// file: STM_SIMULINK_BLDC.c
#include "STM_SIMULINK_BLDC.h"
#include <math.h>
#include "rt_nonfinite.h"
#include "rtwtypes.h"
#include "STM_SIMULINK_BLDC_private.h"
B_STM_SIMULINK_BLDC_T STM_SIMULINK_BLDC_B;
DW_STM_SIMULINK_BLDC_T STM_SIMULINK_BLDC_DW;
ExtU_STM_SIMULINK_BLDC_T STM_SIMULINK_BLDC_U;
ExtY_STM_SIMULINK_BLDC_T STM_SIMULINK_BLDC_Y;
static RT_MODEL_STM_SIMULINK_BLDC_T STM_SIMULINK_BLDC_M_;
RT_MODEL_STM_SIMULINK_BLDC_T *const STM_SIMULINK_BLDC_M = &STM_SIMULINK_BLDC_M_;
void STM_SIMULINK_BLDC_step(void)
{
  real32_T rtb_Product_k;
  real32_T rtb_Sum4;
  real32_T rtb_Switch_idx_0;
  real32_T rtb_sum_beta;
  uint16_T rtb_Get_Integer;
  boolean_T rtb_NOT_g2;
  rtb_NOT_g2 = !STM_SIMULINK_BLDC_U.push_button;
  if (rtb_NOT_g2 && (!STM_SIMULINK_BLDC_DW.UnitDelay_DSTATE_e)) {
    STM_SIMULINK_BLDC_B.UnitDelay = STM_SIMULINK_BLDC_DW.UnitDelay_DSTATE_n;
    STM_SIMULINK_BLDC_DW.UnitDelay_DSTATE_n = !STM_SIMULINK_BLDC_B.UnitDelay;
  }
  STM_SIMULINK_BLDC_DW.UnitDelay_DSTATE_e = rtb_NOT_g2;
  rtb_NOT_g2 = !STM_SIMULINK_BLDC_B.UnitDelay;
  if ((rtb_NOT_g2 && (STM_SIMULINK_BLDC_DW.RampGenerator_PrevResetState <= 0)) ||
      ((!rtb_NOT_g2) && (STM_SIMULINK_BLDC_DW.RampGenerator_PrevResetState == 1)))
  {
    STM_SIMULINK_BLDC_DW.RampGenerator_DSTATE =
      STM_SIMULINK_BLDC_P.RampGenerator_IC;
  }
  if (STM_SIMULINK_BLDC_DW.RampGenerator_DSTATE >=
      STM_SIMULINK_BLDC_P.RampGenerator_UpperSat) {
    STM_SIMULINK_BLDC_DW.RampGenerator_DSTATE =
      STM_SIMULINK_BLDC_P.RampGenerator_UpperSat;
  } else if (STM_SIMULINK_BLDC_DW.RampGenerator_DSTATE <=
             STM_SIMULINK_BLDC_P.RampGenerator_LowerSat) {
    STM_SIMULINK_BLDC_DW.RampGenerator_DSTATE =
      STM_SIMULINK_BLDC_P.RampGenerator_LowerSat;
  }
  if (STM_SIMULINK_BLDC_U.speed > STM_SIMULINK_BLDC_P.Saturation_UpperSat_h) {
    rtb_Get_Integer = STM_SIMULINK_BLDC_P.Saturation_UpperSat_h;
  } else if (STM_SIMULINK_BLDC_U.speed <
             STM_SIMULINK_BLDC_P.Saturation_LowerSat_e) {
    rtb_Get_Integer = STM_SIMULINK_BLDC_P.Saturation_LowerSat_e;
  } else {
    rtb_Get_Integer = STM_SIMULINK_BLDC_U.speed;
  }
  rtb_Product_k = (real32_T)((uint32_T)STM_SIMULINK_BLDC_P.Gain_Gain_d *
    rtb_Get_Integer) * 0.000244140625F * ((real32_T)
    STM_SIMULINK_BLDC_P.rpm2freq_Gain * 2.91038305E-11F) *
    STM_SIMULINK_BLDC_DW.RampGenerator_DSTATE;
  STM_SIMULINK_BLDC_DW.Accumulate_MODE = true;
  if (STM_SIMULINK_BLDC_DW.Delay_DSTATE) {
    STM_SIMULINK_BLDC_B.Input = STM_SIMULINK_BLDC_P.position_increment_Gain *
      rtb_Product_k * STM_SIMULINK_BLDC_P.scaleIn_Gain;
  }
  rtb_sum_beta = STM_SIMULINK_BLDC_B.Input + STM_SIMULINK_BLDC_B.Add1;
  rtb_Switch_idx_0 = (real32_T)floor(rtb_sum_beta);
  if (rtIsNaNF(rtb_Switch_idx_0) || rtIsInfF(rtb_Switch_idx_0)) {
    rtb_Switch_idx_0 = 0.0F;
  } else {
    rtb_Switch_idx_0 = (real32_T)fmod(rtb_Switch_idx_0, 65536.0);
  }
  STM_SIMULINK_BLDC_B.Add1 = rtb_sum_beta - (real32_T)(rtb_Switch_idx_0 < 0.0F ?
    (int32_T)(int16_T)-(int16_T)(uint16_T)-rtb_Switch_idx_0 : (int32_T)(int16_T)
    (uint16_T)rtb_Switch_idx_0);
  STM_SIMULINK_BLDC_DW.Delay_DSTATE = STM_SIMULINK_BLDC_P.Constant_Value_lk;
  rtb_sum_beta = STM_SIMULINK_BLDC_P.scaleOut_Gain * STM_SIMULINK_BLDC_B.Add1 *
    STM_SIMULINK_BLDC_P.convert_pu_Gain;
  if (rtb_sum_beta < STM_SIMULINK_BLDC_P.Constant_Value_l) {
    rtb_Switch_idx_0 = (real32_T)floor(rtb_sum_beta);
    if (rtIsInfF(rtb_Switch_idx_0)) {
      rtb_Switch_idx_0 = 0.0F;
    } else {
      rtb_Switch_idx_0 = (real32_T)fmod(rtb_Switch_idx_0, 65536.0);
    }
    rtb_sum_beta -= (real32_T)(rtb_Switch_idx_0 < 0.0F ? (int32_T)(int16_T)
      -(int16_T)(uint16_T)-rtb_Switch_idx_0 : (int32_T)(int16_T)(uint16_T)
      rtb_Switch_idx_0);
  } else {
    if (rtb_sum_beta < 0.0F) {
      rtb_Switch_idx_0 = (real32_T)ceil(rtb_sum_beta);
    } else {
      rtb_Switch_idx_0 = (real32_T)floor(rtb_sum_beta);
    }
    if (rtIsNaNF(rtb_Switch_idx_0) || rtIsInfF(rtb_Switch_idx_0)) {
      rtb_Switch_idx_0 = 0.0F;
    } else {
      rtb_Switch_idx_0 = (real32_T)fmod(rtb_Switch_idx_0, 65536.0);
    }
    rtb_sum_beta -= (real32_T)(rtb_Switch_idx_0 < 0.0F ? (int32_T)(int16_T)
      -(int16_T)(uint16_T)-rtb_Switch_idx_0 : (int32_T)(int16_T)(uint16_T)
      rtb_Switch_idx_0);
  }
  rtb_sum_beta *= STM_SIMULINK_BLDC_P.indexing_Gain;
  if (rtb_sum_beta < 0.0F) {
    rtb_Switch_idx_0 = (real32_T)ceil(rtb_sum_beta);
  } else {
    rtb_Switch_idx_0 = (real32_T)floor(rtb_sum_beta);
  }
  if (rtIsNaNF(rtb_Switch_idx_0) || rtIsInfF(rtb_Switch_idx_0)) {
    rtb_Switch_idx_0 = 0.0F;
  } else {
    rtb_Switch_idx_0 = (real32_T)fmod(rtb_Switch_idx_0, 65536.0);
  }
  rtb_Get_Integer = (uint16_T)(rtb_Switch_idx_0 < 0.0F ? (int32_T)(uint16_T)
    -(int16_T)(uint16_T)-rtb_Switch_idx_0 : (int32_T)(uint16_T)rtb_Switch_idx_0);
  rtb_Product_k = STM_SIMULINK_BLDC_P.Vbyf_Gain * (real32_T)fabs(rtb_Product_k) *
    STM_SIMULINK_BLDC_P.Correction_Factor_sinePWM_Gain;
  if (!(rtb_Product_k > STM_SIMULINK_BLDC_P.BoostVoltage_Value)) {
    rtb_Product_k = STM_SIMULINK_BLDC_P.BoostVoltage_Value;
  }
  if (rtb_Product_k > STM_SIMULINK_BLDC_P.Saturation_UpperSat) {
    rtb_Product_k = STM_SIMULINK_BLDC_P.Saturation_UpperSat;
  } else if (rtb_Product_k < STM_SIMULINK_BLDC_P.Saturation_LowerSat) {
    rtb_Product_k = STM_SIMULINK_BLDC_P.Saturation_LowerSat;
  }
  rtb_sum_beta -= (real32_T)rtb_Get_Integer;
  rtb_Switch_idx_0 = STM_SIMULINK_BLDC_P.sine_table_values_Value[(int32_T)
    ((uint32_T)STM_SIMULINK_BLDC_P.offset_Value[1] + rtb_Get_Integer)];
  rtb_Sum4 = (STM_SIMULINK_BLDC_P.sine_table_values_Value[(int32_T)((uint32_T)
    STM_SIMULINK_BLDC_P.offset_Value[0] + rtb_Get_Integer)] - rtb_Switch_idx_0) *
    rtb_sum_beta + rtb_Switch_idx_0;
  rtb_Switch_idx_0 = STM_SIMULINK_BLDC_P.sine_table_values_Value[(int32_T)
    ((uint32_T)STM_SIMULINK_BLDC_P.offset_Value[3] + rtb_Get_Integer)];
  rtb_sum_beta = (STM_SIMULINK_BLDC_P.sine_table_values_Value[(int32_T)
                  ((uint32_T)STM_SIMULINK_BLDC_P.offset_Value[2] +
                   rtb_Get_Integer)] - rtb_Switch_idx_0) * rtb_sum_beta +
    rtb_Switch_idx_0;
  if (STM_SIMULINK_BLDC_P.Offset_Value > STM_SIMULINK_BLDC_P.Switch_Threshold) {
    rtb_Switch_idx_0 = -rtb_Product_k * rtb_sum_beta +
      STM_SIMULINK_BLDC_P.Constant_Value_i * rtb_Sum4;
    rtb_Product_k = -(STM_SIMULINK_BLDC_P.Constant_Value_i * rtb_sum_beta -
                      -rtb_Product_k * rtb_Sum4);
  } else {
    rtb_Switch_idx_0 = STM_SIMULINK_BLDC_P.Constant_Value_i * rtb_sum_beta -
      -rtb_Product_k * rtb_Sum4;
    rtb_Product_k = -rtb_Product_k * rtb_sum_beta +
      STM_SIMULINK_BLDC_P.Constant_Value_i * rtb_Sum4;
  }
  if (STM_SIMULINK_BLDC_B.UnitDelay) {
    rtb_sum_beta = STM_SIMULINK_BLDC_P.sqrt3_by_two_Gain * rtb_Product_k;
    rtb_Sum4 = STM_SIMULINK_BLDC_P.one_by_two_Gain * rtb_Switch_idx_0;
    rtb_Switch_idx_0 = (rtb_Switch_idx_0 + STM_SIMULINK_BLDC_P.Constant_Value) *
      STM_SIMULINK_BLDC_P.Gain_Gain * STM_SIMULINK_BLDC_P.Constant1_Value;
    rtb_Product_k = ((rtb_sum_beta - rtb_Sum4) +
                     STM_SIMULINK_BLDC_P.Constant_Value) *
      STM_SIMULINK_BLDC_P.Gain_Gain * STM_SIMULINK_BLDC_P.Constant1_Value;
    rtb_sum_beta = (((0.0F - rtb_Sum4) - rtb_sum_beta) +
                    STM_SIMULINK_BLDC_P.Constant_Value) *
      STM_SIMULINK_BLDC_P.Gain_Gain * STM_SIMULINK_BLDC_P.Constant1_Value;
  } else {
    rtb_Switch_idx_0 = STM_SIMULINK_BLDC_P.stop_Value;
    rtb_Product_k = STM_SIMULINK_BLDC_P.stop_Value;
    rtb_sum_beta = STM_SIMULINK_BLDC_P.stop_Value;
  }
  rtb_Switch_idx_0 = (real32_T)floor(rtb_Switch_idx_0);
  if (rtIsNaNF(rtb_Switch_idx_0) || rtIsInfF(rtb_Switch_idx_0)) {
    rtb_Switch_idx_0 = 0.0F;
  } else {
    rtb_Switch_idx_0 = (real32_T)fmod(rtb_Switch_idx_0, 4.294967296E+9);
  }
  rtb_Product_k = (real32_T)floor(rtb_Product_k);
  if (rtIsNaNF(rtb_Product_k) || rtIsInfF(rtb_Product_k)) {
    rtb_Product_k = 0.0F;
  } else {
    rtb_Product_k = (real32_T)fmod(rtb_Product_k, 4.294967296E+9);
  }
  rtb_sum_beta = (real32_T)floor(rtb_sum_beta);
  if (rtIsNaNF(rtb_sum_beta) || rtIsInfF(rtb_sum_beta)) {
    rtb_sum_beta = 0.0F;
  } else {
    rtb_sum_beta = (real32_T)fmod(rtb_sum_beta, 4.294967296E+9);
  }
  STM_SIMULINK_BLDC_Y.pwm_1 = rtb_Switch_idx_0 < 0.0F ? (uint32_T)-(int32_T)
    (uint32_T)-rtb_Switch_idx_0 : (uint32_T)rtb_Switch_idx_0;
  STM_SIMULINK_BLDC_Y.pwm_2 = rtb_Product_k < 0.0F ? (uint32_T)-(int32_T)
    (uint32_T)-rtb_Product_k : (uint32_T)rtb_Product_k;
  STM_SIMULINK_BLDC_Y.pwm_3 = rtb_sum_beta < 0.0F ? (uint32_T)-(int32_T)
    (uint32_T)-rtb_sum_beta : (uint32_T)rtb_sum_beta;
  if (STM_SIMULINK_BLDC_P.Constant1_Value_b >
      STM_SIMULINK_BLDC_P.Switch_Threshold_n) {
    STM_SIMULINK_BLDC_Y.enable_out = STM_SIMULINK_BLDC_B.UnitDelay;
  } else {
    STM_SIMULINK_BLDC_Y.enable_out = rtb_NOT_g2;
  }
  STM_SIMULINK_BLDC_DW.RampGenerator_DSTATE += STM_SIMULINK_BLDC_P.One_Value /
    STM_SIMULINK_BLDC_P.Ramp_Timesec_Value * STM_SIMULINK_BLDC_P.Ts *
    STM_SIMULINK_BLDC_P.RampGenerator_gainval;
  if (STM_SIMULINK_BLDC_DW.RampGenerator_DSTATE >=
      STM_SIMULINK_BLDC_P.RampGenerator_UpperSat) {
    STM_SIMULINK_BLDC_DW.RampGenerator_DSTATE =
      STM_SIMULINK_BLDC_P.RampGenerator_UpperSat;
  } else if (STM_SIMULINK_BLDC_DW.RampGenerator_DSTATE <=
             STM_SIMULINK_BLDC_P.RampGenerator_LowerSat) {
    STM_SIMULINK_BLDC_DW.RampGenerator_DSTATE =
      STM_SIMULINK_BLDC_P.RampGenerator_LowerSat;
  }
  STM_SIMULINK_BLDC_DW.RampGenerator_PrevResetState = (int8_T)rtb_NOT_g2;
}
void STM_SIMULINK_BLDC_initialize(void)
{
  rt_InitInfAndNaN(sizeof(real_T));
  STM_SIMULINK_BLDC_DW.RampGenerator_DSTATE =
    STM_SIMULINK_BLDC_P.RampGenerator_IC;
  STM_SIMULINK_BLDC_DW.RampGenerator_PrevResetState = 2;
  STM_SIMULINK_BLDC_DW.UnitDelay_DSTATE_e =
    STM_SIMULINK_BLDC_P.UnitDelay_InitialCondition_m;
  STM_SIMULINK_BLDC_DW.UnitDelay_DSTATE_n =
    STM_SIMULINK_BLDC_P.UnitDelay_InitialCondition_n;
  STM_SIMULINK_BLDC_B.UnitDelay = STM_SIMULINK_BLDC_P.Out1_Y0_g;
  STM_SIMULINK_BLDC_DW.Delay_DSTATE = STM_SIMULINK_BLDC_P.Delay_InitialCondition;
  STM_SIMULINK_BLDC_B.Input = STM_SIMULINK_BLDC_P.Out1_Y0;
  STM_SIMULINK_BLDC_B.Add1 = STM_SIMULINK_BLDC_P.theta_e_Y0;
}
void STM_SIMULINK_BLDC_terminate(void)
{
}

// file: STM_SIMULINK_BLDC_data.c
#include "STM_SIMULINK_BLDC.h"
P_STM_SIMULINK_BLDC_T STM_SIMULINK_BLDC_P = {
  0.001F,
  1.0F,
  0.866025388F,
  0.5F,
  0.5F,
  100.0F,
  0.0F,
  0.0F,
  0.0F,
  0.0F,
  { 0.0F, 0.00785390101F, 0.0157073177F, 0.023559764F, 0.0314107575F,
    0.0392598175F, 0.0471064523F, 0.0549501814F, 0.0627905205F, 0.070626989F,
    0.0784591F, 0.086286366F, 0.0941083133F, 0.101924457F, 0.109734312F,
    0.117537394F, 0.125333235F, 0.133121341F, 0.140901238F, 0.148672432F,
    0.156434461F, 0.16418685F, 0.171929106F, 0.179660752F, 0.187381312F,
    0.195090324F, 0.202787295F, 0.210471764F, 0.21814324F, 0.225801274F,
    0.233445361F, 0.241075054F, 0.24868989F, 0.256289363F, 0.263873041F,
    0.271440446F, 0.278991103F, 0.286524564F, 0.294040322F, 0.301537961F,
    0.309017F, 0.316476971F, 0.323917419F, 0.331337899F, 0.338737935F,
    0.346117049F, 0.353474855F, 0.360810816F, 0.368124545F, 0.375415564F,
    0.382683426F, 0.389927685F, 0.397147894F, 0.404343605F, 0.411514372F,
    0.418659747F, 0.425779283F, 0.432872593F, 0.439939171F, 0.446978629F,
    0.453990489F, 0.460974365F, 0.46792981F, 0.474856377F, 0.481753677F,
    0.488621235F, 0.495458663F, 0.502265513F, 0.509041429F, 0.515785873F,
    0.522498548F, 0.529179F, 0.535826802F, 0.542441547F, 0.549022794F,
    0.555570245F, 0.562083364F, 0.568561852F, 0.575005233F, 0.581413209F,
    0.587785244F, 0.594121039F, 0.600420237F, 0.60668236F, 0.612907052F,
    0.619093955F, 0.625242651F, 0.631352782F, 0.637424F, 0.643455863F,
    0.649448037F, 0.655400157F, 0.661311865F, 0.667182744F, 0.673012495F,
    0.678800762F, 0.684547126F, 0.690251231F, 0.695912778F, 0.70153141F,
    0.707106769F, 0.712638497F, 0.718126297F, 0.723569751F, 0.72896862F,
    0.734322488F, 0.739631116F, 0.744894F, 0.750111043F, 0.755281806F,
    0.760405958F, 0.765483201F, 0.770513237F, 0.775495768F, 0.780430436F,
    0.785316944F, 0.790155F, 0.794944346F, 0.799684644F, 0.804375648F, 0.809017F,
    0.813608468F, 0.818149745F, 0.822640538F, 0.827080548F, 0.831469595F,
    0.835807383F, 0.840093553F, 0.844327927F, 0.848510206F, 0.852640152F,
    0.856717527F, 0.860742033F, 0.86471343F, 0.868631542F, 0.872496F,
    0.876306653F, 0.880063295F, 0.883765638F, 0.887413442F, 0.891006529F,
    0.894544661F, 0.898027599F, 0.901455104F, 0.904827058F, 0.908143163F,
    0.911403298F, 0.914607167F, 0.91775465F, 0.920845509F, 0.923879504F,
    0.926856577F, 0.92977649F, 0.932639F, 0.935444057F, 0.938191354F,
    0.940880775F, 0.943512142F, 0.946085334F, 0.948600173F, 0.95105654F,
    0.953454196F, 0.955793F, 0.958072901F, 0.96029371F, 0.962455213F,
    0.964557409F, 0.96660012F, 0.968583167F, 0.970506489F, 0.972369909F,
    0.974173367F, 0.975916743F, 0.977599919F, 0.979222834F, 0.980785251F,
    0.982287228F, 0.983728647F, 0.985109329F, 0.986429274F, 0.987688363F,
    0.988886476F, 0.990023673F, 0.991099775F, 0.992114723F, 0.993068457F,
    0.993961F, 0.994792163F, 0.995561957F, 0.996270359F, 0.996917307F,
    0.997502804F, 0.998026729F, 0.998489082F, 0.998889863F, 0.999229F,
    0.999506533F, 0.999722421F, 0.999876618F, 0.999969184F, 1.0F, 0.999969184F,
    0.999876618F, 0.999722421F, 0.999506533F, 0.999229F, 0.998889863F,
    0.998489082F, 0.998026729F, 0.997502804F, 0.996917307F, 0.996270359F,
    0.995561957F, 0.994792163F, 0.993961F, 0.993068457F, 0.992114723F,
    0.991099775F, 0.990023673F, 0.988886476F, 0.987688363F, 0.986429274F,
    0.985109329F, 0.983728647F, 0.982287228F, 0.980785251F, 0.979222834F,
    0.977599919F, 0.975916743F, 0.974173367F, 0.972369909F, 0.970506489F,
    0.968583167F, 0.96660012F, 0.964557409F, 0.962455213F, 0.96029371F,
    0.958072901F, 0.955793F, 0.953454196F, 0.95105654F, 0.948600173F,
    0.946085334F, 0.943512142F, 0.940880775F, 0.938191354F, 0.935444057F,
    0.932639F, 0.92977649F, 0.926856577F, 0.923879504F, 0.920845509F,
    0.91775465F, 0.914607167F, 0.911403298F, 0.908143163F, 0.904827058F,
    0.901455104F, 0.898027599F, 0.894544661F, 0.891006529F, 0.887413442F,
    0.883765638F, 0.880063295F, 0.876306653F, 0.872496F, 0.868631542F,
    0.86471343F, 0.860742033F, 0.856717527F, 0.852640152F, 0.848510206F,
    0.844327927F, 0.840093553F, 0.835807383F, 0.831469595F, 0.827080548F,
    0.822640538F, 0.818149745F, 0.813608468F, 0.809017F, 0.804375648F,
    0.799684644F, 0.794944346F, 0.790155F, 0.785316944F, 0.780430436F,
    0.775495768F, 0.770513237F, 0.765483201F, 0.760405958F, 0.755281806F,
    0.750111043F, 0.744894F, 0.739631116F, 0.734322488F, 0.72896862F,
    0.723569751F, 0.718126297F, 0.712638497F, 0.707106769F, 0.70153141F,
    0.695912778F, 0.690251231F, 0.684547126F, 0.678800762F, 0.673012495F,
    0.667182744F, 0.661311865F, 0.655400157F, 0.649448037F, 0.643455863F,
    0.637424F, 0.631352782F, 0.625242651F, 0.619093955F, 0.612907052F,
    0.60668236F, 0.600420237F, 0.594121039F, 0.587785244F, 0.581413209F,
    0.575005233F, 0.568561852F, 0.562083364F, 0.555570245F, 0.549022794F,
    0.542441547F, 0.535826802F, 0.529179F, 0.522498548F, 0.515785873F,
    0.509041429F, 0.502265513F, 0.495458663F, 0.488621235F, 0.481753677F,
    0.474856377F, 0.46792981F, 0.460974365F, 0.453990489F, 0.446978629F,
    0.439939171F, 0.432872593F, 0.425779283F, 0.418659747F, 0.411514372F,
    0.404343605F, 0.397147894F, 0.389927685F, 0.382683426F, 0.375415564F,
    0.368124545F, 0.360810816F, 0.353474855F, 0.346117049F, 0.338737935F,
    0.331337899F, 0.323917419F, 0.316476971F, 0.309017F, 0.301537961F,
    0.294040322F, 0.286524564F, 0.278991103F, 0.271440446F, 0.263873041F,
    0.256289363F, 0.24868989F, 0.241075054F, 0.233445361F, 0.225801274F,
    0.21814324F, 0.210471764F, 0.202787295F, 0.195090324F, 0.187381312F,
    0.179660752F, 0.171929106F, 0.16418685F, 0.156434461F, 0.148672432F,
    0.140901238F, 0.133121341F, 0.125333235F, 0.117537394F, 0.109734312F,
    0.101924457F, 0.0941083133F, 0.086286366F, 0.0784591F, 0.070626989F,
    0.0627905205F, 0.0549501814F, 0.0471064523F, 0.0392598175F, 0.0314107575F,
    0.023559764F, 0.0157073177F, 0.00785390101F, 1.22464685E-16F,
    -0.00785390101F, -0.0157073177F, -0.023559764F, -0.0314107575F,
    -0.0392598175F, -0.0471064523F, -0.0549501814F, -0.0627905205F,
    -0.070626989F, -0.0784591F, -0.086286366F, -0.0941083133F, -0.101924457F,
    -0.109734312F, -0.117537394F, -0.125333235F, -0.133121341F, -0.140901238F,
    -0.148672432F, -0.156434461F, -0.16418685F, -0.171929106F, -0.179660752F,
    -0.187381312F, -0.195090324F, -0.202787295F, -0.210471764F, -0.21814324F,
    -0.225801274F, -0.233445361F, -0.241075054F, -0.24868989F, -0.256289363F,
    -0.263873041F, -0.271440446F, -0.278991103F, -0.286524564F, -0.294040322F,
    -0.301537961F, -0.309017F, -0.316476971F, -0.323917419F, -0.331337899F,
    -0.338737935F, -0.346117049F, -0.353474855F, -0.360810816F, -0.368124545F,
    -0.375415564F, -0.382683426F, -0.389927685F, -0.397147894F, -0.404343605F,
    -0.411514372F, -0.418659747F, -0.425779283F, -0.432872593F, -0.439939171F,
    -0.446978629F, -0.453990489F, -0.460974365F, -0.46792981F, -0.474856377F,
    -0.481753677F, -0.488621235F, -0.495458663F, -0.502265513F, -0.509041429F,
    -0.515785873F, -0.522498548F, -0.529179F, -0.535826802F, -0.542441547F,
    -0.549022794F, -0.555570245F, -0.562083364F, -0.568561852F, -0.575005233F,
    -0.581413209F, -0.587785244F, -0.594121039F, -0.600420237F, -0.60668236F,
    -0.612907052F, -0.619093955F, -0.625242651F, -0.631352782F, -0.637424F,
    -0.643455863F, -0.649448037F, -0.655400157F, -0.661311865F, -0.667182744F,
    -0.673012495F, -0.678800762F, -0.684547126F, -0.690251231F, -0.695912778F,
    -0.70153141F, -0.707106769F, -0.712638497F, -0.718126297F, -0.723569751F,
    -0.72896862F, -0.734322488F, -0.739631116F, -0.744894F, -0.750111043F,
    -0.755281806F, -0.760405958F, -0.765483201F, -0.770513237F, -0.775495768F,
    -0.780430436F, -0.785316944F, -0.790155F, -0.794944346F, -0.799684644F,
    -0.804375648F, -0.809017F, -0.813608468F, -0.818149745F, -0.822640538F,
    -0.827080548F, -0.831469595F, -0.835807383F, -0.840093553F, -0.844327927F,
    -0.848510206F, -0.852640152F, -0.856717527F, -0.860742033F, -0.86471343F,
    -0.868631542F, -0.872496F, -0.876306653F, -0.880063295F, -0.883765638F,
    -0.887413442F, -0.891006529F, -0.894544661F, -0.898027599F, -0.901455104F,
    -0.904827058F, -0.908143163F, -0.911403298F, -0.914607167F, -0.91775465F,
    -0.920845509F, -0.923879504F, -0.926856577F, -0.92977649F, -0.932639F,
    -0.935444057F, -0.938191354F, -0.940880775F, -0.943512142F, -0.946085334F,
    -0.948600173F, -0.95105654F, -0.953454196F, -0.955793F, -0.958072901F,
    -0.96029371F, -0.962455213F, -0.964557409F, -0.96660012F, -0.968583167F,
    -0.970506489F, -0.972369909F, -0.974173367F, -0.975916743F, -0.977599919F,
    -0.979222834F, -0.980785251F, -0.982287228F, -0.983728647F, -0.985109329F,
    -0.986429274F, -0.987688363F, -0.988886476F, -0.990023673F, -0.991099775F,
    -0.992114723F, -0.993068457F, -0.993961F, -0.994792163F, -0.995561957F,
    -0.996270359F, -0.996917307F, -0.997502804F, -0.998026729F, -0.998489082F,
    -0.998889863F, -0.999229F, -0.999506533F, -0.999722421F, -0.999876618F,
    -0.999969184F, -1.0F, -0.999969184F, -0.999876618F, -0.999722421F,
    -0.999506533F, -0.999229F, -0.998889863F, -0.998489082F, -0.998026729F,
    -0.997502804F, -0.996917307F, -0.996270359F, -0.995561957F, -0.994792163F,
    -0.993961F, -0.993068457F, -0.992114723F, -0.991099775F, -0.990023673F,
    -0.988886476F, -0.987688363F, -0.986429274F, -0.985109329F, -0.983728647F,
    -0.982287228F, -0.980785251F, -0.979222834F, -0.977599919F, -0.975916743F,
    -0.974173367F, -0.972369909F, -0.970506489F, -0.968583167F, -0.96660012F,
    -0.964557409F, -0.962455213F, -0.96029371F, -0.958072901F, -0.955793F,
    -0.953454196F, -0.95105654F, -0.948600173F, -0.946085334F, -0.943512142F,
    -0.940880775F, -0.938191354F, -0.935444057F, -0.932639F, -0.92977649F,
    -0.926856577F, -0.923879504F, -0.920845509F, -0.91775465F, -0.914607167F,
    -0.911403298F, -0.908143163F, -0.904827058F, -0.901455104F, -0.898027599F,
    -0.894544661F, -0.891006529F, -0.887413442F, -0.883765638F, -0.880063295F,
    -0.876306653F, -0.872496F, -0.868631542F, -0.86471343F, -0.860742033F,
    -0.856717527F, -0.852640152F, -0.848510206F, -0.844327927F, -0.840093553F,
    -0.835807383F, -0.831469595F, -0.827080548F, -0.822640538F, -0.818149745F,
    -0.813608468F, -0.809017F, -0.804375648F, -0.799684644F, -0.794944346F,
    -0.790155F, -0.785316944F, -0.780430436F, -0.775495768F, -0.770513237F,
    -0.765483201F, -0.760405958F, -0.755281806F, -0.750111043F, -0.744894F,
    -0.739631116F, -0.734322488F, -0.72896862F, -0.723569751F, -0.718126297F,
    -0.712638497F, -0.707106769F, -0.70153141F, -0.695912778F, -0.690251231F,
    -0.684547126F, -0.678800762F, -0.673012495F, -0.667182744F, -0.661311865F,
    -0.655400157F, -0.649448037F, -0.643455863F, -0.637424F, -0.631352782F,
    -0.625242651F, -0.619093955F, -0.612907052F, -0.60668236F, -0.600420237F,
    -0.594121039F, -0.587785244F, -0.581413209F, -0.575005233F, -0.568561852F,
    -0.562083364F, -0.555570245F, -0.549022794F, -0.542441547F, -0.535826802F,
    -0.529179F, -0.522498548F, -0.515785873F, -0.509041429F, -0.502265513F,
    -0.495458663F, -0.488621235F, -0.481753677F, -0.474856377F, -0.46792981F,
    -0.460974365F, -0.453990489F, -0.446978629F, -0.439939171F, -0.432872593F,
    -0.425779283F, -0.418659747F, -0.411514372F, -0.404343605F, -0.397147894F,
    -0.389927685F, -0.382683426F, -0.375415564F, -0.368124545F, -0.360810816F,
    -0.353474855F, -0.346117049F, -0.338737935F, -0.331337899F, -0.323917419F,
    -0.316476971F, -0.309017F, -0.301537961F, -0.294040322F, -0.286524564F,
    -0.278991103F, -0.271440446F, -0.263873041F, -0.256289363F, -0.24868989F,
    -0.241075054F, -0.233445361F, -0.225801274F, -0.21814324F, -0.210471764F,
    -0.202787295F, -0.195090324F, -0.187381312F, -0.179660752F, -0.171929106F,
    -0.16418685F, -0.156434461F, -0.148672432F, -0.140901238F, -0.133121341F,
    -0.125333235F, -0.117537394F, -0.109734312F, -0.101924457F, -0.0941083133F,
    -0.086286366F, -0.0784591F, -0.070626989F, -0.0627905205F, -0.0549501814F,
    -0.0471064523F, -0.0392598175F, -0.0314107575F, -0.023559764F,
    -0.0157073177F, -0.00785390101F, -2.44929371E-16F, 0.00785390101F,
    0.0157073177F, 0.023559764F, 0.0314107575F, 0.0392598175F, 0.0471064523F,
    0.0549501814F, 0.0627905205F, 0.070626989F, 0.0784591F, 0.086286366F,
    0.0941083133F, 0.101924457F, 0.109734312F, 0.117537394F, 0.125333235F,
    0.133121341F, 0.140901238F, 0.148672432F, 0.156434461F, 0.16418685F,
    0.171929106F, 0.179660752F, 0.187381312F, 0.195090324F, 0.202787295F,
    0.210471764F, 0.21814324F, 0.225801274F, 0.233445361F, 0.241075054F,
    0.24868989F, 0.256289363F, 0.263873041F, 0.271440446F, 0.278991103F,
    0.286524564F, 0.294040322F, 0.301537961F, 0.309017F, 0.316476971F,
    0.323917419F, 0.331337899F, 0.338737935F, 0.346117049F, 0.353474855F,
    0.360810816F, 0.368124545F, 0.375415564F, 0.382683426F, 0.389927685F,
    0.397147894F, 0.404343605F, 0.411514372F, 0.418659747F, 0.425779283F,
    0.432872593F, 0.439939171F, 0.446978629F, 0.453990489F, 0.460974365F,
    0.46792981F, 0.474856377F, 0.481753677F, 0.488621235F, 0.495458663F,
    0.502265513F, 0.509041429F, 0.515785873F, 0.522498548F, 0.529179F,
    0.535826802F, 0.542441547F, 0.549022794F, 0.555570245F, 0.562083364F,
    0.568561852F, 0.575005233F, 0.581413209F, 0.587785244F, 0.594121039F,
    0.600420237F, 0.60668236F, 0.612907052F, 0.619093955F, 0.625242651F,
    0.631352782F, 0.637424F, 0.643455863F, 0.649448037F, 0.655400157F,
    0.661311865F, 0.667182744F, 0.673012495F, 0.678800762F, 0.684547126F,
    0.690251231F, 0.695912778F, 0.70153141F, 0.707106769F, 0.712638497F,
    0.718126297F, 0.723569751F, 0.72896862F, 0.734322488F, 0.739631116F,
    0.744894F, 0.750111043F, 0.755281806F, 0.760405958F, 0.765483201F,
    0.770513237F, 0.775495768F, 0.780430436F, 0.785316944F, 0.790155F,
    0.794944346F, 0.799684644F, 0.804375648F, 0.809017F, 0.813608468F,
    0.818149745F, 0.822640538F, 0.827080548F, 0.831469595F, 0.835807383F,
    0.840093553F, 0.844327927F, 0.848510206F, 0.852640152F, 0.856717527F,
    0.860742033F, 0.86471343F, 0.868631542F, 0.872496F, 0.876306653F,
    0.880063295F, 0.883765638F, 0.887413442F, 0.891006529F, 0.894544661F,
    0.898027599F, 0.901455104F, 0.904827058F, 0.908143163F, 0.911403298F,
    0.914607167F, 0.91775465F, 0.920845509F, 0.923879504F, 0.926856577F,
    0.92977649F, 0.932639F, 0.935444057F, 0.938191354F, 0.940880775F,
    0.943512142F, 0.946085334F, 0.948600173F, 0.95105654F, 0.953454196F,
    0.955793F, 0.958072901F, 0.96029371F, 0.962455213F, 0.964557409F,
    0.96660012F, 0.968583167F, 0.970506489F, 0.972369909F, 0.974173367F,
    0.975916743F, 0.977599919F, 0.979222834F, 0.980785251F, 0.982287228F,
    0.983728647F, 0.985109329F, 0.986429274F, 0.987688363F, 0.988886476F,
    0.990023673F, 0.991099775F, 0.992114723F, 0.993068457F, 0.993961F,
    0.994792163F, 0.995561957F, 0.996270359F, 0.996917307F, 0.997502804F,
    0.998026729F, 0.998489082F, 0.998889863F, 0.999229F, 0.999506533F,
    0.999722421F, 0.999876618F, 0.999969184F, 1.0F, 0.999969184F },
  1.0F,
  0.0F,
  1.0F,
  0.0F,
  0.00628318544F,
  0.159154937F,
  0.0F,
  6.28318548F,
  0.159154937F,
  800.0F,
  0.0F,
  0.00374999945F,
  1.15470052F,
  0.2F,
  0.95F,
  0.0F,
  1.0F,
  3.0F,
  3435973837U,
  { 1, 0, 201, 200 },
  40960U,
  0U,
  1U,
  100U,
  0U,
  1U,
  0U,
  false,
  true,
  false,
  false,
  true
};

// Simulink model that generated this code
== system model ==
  push_button : Inport
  speed : Inport
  Inport#1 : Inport
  Inport#2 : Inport
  Inport#3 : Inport
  Inport#4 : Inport
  enable_out : Outport  <- 1: Switch
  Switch : Switch  Criteria=u2 > Threshold  <- 1: Subsystem#1, 2: Constant1, 3: NOT
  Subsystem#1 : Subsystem  <- 1: VariantSource#1
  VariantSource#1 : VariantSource  <- 1: DataTypeConversion#1, 2: push_button
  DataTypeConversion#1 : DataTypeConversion  <- 1: Bias#1
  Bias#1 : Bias  Bias=0.5  <- 1: SignalGenerator#1
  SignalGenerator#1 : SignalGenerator  Amplitude=0.5  Frequency=0.5
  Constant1 : Constant  Value=0.5
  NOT : Logic  Operator=NOT  <- 1: Subsystem#1
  pwm_1 : Outport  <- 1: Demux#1
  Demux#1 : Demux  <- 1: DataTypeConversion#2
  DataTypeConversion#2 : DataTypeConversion  <- 1: Switch#1
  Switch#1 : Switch  Threshold=0.5  <- 1: VariantSink#1, 2: Subsystem#1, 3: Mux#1
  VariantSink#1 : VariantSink  <- 1: Product
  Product : Product  <- 1: Gain, 2: Constant#1
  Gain : Gain  Gain=0.5  <- 1: Sum#1
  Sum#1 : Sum  Inputs=++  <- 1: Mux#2, 2: Constant
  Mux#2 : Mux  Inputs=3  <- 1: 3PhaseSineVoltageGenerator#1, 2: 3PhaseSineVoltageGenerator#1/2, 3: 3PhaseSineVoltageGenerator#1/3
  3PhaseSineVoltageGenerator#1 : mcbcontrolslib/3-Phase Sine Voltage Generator  <- 1: Saturation, 2: PositionGenerator#1
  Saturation : Saturate  UpperLimit=0.95  LowerLimit=0  <- 1: Switch#2
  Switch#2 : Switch  Criteria=u2 > Threshold  <- 1: Correction_Factor_sinePWM, 2: RelationalOperator#1, 3: BoostVoltage
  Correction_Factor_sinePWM : Gain  Gain=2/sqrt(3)  <- 1: Vbyf
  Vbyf : Gain  Gain=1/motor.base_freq  <- 1: Abs#1
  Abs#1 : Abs  <- 1: Product#1
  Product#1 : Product  <- 1: rpm2freq, 2: RampGenerator
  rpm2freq : Gain  Gain=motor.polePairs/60  <- 1: VariantSource#2
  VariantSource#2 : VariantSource  <- 1: Constant#2, 2: Gain#1
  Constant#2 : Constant  Value=100
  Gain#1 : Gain  Gain=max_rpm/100  <- 1: Saturate#1
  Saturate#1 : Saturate  UpperLimit=100  LowerLimit=0  <- 1: speed
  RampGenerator : DiscreteIntegrator  IntegratorMethod=Accumulation: Forward Euler  gainval=1  ExternalReset=either  LimitOutput=on  UpperSaturationLimit=1  LowerSaturationLimit=0  <- 1: Gain#2, 2: Logic#1
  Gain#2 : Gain  Gain=Ts  <- 1: Product#2
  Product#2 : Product  Inputs=*/  <- 1: One, 2: Ramp_Timesec
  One : Constant
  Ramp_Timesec : Constant  Value=3
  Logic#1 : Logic  Operator=NOT  <- 1: Subsystem#1
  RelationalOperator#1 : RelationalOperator  Operator=>  <- 1: Correction_Factor_sinePWM, 2: BoostVoltage
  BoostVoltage : Constant  Value=0.2
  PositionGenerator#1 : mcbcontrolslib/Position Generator  ExternalReset=none  <- 1: position_increment
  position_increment : Gain  Gain=2*pi*Ts  <- 1: Product#1
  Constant : Constant
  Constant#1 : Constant  Value=100
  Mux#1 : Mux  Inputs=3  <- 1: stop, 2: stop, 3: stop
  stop : Constant  Value=0
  pwm_2 : Outport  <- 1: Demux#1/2
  pwm_3 : Outport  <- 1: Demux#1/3
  Product#3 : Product  <- 1: Subsystem#1, 2: VariantSink#1/2
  Gain#3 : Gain
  Constant#3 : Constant
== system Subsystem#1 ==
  Inport#5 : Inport
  Out1 : Outport  <- 1: Subsystem#2
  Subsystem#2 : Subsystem  <- Enable: Logic#2
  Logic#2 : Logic  <- 1: Logic#3, 2: Logic#4
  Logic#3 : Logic  Operator=NOT  <- 1: Inport#5
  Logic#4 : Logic  Operator=NOT  <- 1: UnitDelay
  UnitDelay : UnitDelay  InitialCondition=false  <- 1: Logic#3
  Constant#4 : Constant
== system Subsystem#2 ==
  EnablePort#1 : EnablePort
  Outport#1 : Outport  <- 1: UnitDelay#1
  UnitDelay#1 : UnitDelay  InitialCondition=true  <- 1: Logic#5
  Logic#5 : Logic  Operator=NOT  <- 1: UnitDelay#1
